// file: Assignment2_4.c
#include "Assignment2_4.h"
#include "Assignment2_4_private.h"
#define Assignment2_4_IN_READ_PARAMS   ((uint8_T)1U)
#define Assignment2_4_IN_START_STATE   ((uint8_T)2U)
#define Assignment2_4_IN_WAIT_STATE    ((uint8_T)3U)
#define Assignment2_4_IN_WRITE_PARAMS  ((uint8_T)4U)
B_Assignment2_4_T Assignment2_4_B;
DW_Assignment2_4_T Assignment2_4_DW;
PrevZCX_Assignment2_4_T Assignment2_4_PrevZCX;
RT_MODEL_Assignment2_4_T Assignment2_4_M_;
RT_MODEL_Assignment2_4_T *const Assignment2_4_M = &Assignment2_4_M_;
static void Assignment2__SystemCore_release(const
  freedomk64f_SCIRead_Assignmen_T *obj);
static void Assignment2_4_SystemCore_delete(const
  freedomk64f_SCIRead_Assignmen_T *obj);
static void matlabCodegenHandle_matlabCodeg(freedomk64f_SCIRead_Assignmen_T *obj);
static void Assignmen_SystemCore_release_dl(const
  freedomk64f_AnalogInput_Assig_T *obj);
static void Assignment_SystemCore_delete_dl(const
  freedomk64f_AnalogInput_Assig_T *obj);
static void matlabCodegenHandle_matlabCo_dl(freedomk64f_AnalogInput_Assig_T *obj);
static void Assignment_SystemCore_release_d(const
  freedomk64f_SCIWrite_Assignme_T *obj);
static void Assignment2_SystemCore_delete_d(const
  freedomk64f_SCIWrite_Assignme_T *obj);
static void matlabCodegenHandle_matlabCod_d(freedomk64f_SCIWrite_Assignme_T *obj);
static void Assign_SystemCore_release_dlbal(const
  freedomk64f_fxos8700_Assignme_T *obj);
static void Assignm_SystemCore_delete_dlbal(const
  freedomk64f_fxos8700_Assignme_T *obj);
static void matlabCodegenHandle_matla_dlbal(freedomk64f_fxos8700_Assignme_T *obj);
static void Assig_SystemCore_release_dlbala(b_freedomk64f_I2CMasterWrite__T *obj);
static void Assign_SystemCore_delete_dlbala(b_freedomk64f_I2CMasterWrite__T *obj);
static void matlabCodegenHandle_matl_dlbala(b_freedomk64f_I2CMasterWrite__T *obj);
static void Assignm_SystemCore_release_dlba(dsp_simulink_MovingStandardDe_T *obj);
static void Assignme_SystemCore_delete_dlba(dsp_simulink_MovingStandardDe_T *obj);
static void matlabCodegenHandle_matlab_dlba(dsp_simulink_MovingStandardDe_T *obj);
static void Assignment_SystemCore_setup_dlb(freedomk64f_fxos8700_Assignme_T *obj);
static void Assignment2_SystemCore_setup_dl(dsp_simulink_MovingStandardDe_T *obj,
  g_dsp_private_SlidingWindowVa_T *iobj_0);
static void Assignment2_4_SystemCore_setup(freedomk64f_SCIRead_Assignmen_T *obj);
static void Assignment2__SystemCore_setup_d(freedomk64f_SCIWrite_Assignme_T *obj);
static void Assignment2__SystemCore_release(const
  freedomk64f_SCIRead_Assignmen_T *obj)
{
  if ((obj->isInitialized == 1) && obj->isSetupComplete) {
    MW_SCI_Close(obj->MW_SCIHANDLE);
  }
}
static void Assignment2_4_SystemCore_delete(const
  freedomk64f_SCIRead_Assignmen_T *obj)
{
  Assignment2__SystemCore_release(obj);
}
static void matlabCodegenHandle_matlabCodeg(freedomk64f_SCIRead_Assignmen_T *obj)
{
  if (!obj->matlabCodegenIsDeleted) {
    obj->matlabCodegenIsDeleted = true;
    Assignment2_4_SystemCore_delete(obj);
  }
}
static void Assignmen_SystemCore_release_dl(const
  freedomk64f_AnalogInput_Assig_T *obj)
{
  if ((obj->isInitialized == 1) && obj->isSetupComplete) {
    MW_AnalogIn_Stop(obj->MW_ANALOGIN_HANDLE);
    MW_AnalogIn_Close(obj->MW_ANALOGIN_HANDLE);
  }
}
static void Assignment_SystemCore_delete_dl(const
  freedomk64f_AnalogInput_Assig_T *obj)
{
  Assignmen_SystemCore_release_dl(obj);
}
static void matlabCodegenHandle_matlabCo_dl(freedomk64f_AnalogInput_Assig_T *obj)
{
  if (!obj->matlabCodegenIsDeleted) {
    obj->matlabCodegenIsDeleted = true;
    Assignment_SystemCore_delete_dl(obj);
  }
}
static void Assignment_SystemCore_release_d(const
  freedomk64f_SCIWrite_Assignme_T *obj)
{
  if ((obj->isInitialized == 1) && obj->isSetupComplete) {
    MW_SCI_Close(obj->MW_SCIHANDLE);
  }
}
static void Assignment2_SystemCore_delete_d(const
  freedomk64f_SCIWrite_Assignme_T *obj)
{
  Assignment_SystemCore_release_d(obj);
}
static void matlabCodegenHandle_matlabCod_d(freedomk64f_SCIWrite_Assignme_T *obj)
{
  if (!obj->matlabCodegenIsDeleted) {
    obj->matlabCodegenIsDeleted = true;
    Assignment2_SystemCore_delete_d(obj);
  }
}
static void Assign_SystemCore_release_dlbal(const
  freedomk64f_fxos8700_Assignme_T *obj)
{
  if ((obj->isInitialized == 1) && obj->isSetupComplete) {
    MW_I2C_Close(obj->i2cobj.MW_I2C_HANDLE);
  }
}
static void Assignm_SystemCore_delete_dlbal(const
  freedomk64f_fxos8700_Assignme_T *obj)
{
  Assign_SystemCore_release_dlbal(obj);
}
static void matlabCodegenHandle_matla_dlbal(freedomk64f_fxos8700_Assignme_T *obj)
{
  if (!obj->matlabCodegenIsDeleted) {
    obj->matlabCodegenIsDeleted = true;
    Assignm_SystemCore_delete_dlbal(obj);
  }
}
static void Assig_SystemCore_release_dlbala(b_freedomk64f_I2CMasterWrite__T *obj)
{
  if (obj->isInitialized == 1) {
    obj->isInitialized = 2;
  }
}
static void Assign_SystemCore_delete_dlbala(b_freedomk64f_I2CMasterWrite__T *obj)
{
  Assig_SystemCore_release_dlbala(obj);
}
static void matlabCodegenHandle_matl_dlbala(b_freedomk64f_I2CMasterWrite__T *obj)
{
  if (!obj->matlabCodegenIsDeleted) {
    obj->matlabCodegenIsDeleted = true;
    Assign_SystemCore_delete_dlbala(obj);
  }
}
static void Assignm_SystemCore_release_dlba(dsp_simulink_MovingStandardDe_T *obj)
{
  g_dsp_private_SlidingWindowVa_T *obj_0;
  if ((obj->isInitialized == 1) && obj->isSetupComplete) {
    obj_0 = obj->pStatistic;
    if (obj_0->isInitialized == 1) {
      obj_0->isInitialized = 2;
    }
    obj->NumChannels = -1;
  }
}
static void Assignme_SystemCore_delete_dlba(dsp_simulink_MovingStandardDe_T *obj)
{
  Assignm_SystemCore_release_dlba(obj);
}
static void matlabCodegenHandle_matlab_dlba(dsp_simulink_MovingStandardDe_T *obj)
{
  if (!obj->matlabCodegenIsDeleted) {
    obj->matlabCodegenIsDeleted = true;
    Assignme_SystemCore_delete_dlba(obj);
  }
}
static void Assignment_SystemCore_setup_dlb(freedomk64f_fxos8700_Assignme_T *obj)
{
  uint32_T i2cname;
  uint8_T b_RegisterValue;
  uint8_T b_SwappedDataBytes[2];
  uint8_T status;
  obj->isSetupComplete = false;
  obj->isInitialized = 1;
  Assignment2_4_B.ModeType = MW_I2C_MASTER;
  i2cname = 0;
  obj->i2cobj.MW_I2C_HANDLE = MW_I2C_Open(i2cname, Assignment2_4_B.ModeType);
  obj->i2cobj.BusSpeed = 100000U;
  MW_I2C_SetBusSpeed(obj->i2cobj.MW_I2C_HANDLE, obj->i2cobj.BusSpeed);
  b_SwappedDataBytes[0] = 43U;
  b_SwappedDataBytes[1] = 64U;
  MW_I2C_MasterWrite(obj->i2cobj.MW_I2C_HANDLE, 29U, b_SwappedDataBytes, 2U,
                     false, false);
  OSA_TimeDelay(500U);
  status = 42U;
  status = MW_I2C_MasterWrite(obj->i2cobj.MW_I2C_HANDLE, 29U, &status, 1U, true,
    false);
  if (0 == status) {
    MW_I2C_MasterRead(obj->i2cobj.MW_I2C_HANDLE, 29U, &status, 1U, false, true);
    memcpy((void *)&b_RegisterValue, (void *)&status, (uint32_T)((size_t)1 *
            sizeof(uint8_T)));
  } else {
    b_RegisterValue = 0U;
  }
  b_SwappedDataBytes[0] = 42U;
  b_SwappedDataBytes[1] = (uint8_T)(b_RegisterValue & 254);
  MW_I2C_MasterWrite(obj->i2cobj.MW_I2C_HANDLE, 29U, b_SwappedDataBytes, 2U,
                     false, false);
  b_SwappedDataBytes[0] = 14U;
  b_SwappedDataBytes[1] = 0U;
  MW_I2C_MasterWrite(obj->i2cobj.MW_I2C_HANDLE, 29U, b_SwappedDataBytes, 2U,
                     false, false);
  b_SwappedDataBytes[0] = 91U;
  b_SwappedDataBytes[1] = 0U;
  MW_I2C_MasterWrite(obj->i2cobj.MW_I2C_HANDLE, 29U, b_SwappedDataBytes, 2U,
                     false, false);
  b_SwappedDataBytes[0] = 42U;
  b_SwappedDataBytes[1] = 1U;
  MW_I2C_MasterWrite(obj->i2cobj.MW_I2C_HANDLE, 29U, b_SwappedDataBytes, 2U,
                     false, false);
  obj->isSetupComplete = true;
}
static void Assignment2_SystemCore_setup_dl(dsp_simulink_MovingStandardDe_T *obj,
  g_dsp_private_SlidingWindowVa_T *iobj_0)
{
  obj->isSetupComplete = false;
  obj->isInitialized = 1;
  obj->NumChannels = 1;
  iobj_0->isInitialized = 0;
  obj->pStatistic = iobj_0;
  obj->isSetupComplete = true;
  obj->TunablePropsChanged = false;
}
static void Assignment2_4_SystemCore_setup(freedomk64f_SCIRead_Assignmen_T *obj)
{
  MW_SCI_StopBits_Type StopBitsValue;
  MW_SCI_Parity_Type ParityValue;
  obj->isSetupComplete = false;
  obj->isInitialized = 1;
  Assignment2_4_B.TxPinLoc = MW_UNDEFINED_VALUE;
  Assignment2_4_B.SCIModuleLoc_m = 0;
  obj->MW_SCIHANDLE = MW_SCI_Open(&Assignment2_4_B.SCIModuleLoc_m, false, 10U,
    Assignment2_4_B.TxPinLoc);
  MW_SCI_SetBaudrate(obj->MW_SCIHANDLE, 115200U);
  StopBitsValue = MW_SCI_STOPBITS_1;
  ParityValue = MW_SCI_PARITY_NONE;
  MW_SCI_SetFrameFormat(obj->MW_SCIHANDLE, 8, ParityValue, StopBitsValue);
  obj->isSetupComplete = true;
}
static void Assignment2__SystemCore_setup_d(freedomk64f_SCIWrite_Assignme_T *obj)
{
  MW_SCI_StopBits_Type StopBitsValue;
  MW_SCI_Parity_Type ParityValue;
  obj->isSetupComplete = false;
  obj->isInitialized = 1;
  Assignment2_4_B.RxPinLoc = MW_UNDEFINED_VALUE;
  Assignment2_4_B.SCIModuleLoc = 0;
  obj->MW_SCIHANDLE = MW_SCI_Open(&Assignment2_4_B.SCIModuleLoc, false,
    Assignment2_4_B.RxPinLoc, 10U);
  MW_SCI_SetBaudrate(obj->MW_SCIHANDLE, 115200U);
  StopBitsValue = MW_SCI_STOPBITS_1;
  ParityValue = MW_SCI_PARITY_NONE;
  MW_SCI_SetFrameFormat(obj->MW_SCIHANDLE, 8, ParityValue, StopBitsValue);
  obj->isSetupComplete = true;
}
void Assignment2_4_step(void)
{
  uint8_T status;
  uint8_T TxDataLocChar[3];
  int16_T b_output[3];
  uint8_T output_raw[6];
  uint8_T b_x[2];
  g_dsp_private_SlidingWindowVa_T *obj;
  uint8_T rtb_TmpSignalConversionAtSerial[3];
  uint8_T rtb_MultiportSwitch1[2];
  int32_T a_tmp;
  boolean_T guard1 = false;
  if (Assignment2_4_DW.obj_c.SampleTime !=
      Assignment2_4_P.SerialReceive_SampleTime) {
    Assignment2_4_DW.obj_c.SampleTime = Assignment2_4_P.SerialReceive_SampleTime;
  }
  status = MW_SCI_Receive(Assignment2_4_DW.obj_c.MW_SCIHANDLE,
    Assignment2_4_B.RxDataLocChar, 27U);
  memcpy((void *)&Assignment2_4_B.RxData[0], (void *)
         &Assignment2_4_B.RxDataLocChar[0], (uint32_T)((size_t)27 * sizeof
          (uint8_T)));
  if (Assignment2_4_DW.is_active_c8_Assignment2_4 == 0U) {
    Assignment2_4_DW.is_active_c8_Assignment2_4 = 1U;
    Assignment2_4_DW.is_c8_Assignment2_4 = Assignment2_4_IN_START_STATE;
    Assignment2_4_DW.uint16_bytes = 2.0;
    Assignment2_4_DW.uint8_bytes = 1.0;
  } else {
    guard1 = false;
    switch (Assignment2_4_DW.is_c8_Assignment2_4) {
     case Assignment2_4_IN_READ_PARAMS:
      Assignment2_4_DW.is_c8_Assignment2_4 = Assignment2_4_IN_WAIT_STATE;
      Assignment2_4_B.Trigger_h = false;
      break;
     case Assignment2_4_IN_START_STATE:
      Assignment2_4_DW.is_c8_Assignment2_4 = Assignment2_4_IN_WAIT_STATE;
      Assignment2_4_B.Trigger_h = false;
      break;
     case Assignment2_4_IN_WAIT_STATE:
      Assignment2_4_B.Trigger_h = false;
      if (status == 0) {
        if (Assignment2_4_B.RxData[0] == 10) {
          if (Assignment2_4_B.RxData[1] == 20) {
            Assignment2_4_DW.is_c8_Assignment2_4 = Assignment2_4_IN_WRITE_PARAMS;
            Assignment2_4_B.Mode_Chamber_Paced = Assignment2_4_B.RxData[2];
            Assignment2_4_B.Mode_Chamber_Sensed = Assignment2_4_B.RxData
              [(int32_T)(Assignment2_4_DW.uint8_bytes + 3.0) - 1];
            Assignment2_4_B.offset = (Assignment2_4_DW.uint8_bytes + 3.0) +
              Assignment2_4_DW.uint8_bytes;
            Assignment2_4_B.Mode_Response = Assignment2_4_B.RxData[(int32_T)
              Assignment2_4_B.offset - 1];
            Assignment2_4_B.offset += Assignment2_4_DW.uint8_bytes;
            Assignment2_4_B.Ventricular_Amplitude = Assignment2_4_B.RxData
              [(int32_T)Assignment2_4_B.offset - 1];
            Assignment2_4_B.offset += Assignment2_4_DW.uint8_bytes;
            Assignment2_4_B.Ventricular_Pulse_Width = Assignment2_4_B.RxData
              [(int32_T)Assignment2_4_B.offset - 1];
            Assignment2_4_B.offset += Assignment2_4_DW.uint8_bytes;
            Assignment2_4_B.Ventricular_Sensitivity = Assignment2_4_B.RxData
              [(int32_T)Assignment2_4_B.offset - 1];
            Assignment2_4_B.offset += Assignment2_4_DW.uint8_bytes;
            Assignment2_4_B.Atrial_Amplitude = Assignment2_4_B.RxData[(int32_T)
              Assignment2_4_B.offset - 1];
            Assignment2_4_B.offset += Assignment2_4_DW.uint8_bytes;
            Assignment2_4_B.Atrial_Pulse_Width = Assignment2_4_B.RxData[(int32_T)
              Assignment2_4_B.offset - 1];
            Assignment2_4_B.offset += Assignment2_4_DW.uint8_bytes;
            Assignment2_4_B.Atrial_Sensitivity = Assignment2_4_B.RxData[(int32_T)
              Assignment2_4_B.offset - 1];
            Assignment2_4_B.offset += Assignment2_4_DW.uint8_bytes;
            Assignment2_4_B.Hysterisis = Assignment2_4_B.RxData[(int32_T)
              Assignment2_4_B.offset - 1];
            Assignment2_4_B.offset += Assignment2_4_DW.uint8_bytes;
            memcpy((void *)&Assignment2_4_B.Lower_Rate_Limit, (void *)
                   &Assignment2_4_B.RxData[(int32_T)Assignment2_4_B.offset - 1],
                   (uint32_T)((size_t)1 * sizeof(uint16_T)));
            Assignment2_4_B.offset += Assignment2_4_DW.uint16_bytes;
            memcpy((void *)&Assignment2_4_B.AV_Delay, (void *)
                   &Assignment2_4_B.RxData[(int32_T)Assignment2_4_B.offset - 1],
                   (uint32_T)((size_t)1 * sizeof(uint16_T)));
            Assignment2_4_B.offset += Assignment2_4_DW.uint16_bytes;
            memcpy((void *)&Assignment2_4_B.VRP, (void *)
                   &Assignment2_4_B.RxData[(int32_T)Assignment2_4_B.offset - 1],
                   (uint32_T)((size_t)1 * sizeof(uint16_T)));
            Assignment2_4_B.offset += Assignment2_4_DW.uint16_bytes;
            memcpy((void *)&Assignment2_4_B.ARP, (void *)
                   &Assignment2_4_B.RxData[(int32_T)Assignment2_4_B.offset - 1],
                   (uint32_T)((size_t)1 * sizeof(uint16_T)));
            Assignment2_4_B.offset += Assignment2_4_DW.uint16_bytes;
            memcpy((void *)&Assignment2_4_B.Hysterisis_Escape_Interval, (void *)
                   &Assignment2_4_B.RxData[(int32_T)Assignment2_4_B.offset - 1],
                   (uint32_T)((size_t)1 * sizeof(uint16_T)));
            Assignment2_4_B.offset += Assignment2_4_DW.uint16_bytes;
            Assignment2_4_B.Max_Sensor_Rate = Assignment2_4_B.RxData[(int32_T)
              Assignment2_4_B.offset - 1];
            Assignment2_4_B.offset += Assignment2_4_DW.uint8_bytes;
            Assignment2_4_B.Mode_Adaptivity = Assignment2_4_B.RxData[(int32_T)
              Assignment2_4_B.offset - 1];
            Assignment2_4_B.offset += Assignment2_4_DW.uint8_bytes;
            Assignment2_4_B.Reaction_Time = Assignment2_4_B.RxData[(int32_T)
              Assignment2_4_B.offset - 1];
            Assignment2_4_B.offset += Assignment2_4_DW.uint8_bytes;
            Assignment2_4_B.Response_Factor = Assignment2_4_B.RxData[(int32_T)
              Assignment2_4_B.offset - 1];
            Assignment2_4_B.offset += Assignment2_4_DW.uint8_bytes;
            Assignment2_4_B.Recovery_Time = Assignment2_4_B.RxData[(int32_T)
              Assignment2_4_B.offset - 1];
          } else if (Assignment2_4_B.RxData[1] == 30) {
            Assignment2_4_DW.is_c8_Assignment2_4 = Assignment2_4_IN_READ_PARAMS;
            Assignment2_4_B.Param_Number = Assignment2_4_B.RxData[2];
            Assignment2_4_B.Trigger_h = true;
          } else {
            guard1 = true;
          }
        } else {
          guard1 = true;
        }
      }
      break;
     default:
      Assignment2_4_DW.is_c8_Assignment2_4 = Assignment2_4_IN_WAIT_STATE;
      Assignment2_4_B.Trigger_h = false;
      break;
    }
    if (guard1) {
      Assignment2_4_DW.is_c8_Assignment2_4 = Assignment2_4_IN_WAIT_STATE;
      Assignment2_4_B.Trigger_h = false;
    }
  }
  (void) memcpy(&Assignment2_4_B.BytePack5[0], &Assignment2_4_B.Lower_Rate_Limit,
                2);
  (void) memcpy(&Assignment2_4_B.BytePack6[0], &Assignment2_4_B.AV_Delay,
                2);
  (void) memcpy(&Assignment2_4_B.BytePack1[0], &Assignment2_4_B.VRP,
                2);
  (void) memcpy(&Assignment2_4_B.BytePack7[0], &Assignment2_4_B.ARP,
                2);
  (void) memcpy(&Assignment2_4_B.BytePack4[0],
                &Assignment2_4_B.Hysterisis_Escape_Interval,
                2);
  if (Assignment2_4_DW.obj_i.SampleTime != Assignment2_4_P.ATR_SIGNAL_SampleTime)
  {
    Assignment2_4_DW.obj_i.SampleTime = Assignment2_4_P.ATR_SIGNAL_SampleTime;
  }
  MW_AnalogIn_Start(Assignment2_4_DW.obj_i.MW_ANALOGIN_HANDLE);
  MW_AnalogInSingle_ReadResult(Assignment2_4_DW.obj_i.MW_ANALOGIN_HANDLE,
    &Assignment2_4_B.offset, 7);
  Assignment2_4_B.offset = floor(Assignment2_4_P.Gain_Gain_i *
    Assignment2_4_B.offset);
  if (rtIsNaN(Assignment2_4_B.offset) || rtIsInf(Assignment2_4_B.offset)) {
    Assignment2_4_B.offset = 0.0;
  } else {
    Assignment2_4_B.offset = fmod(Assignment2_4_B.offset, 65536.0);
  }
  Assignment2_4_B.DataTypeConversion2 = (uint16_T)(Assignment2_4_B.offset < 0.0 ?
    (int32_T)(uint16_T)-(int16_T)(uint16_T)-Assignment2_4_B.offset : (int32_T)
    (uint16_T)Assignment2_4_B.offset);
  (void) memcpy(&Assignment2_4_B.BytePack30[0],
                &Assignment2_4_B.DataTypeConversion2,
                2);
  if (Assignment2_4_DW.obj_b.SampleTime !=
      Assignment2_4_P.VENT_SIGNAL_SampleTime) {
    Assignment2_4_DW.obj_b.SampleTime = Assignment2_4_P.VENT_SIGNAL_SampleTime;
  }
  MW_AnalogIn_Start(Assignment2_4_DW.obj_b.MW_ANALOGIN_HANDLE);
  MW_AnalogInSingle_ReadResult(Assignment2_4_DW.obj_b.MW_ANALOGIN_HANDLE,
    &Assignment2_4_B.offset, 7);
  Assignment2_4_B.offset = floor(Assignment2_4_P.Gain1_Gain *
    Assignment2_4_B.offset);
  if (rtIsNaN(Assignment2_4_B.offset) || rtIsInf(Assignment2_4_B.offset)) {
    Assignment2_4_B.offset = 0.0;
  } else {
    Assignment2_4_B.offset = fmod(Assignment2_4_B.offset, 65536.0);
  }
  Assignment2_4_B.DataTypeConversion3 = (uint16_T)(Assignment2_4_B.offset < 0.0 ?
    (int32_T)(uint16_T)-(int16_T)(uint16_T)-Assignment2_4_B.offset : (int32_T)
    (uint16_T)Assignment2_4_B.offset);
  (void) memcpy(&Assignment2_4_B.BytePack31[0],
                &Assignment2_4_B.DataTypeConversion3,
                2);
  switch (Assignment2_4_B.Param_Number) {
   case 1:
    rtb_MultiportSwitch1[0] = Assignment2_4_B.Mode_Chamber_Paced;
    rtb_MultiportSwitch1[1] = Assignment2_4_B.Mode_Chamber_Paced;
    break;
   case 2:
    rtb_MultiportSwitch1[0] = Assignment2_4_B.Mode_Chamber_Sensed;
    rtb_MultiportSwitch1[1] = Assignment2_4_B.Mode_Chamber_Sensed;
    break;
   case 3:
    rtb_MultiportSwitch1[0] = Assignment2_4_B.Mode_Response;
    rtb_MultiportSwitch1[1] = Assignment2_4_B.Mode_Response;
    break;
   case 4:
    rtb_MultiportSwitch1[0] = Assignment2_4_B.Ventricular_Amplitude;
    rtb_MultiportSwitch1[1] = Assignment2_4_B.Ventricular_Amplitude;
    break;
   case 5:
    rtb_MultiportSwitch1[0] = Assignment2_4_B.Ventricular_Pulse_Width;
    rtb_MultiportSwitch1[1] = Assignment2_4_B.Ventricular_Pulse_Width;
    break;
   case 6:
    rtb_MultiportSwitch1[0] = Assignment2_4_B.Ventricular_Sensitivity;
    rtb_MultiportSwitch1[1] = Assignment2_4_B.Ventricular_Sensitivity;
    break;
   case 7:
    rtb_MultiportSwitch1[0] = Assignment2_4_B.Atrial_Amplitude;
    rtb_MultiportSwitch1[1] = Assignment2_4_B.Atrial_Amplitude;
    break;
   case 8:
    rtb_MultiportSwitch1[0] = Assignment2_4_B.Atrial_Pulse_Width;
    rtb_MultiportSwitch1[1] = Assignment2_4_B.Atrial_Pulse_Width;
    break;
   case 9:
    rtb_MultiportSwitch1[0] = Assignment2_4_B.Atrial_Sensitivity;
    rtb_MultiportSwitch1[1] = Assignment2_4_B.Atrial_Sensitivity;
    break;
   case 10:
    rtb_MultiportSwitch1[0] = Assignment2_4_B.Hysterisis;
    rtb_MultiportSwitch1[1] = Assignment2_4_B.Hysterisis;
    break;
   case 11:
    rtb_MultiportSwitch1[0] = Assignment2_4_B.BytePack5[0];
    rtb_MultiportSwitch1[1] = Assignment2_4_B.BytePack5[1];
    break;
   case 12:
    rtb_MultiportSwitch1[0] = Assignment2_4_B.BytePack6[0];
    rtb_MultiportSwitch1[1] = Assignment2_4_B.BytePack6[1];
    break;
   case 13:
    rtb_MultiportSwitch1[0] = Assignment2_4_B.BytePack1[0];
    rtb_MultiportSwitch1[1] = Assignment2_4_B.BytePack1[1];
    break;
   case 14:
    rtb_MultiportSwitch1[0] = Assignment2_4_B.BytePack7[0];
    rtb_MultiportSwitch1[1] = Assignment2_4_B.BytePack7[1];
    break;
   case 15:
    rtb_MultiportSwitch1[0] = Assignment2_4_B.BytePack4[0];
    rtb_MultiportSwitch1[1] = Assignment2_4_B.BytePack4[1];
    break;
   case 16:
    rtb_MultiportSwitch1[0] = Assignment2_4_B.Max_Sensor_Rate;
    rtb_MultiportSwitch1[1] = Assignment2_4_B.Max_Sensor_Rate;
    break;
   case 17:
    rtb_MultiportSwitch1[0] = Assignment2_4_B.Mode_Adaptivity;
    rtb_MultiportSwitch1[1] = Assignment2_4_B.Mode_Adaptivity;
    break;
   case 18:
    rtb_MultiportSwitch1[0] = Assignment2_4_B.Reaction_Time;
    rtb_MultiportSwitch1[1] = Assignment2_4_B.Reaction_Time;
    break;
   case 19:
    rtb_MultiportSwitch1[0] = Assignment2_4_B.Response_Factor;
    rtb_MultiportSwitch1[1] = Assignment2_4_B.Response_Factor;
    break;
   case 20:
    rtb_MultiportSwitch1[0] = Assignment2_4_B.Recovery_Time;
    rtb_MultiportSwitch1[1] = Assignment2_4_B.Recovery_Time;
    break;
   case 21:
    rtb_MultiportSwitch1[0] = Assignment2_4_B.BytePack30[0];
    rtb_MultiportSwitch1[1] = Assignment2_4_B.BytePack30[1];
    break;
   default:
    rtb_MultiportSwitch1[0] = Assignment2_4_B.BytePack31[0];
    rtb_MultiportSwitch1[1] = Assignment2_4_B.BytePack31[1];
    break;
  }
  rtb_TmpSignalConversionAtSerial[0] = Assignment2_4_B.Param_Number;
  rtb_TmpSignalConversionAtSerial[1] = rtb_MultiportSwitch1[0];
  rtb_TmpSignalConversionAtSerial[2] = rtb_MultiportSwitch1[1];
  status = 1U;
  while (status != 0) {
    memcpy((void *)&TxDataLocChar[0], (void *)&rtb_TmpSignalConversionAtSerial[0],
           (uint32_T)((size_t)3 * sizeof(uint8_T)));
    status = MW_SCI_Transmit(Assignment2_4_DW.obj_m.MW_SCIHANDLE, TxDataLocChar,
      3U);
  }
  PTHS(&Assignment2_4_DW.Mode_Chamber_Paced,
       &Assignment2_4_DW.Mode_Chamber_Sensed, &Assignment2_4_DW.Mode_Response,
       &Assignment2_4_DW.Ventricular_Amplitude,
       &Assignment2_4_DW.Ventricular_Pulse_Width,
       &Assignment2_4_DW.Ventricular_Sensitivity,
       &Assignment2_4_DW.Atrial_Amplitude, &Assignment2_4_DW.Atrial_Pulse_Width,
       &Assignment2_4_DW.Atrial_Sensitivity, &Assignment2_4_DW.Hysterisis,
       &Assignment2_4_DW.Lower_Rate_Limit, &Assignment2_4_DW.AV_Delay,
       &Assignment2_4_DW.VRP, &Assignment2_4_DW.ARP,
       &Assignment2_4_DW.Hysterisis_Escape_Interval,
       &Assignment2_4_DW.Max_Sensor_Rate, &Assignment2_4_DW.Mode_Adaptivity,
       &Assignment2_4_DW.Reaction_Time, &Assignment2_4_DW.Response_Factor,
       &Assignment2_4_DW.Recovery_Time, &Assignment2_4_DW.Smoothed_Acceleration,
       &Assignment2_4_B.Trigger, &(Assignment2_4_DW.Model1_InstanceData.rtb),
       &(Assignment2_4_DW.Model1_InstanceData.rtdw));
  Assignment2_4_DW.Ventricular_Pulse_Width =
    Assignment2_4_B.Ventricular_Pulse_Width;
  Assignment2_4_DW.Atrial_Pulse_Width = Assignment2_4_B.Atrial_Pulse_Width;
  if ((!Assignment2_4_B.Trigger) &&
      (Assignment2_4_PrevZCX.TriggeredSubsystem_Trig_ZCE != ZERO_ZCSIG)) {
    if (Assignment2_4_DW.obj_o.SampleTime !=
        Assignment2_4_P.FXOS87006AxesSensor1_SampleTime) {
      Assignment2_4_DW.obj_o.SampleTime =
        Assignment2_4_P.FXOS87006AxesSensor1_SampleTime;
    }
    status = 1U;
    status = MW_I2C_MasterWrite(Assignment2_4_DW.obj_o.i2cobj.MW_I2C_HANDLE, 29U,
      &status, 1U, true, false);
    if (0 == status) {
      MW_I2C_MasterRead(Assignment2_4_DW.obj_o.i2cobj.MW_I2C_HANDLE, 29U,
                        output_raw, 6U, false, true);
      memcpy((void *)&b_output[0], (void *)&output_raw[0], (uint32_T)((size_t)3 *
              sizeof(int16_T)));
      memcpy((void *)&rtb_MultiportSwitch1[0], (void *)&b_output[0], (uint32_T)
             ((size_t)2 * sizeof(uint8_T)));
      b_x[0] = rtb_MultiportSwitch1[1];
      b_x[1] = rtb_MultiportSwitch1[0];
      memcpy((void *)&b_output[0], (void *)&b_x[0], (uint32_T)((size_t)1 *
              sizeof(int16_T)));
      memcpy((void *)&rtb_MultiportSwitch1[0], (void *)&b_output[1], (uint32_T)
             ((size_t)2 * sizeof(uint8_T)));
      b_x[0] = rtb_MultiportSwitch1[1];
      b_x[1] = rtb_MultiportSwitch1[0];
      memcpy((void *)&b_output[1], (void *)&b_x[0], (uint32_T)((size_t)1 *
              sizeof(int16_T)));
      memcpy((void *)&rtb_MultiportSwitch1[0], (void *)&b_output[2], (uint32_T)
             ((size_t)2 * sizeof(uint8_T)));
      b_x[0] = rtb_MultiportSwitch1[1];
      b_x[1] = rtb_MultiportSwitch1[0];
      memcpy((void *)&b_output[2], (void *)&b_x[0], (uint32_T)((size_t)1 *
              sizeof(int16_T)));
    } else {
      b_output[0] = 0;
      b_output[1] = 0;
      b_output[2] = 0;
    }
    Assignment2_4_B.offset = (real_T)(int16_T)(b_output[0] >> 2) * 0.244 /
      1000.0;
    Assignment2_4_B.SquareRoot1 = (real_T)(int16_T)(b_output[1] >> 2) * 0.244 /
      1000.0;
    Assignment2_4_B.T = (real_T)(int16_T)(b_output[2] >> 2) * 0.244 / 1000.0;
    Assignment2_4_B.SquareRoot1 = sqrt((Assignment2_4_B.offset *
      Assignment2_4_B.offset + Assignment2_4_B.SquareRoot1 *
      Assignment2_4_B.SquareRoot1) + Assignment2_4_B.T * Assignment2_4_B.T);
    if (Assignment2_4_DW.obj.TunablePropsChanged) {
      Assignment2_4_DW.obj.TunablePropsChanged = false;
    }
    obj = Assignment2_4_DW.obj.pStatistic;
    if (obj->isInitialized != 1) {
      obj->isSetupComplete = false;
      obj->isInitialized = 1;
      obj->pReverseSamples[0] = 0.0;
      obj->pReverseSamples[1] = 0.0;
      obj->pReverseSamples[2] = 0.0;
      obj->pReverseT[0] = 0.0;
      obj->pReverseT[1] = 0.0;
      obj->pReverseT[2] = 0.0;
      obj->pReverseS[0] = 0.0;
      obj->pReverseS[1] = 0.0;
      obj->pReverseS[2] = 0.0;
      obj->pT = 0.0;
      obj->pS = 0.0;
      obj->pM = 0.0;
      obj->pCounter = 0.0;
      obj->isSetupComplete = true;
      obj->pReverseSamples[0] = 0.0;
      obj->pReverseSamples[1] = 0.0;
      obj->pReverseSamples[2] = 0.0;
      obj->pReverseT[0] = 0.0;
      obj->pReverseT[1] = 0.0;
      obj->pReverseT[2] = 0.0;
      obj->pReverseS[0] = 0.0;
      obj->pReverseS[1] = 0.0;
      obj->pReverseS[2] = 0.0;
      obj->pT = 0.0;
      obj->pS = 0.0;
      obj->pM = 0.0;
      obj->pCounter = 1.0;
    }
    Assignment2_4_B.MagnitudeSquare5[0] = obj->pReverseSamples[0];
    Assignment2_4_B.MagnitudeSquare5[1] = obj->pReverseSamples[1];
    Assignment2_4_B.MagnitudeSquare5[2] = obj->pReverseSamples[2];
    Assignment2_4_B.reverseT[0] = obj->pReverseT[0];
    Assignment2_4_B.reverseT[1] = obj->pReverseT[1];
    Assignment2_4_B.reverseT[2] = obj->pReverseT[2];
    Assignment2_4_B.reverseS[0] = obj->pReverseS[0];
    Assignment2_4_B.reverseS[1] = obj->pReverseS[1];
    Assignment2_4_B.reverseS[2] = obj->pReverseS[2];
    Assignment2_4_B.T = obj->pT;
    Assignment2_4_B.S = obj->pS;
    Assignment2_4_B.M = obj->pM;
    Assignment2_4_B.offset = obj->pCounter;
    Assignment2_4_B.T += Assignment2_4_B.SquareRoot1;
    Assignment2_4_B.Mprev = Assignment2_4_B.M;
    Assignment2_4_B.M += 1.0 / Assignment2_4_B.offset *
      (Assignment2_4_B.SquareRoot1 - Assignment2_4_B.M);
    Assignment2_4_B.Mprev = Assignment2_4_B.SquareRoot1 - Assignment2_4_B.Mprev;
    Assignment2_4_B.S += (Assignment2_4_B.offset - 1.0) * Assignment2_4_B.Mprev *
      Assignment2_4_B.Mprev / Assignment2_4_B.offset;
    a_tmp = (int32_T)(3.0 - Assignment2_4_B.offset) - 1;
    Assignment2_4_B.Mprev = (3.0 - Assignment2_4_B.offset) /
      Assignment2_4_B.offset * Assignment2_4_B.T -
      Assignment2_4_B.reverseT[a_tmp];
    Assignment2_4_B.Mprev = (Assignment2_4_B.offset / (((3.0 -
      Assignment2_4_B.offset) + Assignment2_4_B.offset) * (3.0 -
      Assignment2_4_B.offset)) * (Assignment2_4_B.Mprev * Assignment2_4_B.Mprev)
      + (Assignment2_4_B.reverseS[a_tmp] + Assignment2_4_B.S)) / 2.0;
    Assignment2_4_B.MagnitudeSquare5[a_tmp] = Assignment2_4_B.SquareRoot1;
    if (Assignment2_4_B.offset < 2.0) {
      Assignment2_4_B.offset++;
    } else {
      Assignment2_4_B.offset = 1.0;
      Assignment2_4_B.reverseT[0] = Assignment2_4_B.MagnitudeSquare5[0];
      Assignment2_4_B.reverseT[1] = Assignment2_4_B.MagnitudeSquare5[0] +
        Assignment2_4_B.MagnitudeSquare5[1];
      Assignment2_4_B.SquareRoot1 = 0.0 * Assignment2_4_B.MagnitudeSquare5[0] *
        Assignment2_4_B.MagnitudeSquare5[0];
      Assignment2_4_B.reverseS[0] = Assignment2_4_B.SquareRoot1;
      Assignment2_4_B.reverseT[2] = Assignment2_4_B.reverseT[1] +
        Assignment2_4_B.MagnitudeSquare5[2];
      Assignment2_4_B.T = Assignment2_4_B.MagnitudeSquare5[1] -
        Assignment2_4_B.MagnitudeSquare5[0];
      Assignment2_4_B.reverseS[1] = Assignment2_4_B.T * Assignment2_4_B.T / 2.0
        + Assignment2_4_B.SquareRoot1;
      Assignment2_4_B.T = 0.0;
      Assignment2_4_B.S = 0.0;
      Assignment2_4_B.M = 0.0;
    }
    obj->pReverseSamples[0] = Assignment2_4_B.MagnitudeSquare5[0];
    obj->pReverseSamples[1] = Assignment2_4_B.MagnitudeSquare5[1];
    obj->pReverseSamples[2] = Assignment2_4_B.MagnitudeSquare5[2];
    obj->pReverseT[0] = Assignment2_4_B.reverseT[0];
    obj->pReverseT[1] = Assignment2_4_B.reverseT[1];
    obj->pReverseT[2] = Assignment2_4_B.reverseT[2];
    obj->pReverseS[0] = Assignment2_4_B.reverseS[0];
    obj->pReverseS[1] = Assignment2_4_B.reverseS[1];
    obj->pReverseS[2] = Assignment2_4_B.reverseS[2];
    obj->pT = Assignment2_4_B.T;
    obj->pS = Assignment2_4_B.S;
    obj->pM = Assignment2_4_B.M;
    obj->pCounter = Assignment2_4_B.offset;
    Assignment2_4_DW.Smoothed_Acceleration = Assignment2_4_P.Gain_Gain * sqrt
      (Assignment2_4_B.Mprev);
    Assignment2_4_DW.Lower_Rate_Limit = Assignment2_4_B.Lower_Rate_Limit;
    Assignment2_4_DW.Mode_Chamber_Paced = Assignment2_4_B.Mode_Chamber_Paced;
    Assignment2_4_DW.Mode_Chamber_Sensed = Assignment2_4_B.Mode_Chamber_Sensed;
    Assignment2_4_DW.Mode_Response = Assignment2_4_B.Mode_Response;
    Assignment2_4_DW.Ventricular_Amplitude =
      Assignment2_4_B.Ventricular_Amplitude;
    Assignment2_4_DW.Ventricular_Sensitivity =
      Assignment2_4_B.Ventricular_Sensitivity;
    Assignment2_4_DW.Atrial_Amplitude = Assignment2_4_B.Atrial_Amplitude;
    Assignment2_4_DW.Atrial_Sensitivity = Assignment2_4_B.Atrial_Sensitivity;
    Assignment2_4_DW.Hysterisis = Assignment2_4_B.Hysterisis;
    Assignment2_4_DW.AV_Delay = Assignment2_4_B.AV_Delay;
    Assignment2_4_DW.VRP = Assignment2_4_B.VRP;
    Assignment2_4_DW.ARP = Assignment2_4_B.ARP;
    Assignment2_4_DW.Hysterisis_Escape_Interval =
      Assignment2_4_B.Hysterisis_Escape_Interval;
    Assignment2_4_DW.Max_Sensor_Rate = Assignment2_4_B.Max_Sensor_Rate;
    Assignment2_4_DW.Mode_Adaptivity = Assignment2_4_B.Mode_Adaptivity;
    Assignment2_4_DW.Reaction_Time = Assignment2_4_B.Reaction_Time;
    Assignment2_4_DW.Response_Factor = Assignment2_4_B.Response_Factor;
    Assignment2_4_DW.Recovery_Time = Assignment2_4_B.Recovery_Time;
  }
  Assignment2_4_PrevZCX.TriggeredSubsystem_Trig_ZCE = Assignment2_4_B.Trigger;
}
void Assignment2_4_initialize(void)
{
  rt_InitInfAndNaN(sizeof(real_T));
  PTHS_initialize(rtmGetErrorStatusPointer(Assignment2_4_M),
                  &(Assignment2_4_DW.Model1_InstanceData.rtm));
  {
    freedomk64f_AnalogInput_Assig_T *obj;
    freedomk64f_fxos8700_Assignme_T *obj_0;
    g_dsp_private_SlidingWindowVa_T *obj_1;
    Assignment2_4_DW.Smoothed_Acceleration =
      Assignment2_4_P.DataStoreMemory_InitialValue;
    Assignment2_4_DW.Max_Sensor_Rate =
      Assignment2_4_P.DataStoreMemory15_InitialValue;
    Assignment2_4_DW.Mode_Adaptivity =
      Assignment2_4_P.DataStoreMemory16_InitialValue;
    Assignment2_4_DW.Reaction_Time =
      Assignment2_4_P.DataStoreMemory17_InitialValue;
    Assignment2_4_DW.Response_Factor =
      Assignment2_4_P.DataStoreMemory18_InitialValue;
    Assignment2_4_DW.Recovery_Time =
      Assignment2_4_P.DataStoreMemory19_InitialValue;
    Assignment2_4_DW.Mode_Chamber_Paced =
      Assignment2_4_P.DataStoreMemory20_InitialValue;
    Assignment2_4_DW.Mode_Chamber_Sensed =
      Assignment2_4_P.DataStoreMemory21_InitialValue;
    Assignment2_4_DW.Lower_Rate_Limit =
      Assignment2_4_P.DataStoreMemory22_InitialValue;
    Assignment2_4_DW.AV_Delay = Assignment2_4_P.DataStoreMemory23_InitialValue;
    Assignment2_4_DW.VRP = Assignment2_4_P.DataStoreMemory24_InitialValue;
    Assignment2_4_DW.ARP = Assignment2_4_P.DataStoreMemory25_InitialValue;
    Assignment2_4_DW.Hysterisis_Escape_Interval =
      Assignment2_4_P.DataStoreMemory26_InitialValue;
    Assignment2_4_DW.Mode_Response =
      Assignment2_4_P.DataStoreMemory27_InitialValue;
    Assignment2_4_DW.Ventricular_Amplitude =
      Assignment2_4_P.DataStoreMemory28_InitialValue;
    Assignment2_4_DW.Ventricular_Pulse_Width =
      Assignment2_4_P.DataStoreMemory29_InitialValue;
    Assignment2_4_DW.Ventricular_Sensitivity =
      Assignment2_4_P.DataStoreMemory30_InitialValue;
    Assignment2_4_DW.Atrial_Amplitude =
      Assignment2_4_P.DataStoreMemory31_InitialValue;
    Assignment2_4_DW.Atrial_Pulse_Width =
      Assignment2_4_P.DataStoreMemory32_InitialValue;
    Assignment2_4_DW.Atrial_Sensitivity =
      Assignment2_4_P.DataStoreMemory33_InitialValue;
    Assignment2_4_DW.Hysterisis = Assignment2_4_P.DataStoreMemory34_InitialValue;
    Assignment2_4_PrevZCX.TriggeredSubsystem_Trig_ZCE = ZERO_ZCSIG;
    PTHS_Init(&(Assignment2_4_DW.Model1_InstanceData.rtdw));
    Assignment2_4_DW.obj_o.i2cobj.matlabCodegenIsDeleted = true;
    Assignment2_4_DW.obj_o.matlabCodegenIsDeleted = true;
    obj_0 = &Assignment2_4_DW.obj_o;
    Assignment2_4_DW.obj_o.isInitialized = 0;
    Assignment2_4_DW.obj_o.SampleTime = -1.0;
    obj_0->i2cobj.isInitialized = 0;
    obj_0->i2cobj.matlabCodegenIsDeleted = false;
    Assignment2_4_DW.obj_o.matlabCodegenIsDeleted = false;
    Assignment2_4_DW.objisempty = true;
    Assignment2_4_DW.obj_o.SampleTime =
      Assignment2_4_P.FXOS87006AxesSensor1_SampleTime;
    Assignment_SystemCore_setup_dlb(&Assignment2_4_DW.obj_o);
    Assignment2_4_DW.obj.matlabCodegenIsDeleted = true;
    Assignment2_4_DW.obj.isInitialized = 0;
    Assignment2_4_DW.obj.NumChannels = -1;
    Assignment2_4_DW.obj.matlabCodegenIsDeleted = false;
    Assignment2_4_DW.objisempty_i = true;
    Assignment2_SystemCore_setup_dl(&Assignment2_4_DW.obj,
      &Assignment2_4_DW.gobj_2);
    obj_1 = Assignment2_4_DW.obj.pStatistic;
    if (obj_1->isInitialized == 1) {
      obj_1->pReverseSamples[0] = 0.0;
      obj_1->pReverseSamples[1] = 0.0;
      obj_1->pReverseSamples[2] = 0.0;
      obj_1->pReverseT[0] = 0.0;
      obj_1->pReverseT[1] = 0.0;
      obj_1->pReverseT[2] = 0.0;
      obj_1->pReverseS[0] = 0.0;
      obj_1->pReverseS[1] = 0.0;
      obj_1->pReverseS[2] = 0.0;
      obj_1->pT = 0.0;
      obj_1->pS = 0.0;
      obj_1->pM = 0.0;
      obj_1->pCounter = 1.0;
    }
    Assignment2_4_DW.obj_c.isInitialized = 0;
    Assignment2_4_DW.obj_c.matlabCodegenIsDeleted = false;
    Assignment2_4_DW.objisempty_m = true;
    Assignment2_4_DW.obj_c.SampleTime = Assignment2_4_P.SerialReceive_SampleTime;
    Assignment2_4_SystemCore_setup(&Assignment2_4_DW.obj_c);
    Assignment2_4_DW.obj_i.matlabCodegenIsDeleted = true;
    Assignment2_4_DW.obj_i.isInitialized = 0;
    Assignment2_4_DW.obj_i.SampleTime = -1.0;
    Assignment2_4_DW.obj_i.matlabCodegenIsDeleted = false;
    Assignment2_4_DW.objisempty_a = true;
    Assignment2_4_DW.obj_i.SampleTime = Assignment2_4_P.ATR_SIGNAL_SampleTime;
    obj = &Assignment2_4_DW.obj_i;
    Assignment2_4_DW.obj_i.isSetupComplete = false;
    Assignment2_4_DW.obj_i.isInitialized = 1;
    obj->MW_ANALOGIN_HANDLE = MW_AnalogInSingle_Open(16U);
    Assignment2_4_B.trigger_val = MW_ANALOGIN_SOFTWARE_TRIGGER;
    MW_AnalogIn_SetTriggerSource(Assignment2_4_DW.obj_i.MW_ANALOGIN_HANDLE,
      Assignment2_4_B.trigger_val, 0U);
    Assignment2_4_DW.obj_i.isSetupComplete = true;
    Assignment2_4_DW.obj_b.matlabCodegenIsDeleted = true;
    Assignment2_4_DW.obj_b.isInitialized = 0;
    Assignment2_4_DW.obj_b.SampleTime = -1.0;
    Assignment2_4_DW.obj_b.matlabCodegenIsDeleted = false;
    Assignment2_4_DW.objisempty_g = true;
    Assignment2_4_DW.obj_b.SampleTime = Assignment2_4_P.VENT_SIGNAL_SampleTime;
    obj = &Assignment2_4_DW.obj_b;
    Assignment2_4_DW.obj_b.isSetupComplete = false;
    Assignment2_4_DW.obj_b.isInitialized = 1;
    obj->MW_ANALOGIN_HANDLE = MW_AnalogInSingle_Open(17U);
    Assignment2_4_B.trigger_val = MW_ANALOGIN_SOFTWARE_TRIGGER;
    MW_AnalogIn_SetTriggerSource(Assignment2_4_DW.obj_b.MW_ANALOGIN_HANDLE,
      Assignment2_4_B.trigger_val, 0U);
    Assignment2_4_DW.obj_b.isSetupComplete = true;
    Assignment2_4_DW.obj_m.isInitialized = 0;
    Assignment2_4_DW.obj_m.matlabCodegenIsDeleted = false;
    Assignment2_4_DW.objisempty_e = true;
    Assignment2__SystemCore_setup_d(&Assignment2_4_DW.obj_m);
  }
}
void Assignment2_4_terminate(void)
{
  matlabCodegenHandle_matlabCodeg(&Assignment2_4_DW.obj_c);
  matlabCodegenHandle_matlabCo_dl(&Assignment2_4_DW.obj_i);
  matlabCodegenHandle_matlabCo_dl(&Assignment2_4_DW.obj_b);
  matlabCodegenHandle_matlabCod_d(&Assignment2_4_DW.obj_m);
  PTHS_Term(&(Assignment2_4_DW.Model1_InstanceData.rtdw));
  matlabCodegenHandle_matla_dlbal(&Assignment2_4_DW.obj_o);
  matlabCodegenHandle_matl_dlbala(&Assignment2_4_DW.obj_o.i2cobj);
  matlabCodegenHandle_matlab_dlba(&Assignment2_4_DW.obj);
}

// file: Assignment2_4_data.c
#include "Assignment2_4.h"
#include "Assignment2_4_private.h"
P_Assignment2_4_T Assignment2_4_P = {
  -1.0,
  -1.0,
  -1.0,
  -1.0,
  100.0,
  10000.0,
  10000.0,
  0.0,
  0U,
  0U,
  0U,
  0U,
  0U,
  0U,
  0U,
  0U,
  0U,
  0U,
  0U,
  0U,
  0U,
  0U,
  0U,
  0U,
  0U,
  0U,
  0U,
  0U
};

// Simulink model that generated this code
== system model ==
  SerialTransmit#1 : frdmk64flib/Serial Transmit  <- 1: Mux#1
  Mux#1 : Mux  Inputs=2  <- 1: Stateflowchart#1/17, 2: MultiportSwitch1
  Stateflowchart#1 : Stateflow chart  <- 1: SerialReceive, 2: SerialReceive/2
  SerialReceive : frdmk64flib/Serial Receive
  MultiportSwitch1 : MultiPortSwitch  Inputs=22  <- 1: Stateflowchart#1/17, 2: Stateflowchart#1/2, 3: Stateflowchart#1/3, 4: Stateflowchart#1/4, 5: Stateflowchart#1/5, 6: Stateflowchart#1/6, 7: Stateflowchart#1/7, 8: Stateflowchart#1/8, 9: Stateflowchart#1/9, 10: Stateflowchart#1/10, 11: Stateflowchart#1/11, 12: BytePack5, 13: BytePack6, 14: BytePack1, 15: BytePack7, 16: BytePack4, 17: Stateflowchart#1/18, 18: Stateflowchart#1/19, 19: Stateflowchart#1/20, 20: Stateflowchart#1/21, 21: Stateflowchart#1/22, 22: BytePack30, 23: BytePack31
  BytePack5 : etargetslib/Byte Pack  <- 1: Stateflowchart#1/12
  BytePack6 : etargetslib/Byte Pack  <- 1: Stateflowchart#1/13
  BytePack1 : etargetslib/Byte Pack  <- 1: Stateflowchart#1/14
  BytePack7 : etargetslib/Byte Pack  <- 1: Stateflowchart#1/15
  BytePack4 : etargetslib/Byte Pack  <- 1: Stateflowchart#1/16
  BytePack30 : etargetslib/Byte Pack  <- 1: DataTypeConversion2
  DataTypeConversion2 : DataTypeConversion  <- 1: Gain
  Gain : Gain  Gain=10000  <- 1: ATR_SIGNAL
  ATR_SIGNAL : frdmk64flib/Analog Input
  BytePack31 : etargetslib/Byte Pack  <- 1: DataTypeConversion3
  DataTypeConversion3 : DataTypeConversion  <- 1: Gain1
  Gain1 : Gain  Gain=10000  <- 1: VENT_SIGNAL
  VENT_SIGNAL : frdmk64flib/Analog Input
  TriggeredSubsystem : Subsystem  <- 1: Stateflowchart#1/2, 2: Stateflowchart#1/3, 3: Stateflowchart#1/4, 4: Stateflowchart#1/5, 5: DataTypeConversion#1, 6: Stateflowchart#1/7, 7: Stateflowchart#1/8, 8: DataTypeConversion#2, 9: Stateflowchart#1/10, 10: Stateflowchart#1/11, 11: Stateflowchart#1/12, 12: Stateflowchart#1/13, 13: Stateflowchart#1/14, 14: Stateflowchart#1/15, 15: Stateflowchart#1/16, 16: Stateflowchart#1/18, 17: Stateflowchart#1/19, 18: Stateflowchart#1/20, 19: Stateflowchart#1/21, 20: Stateflowchart#1/22, Trigger: Model1
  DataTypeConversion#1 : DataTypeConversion  <- 1: Stateflowchart#1/6
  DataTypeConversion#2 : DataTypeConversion  <- 1: Stateflowchart#1/9
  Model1 : ModelReference  <- 1: DataStoreRead#1, 2: DataStoreRead#2, 3: DataStoreRead#3, 4: DataStoreRead#4, 5: DataStoreRead#5, 6: DataStoreRead#6, 7: DataStoreRead#7, 8: DataStoreRead#8, 9: DataStoreRead#9, 10: DataStoreRead#10, 11: DataStoreRead#11, 12: DataStoreRead#12, 13: DataStoreRead#13, 14: DataStoreRead#14, 15: DataStoreRead#15, 16: DataStoreRead#16, 17: DataStoreRead#17, 18: DataStoreRead#18, 19: DataStoreRead#19, 20: DataStoreRead#20, 21: DataStoreRead#21
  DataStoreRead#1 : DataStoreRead  DataStoreName=Mode_Chamber_Paced
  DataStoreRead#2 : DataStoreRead  DataStoreName=Mode_Chamber_Sensed
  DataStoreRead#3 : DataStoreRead  DataStoreName=Mode_Response
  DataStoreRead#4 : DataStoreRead  DataStoreName=Ventricular_Amplitude
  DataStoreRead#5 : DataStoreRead  DataStoreName=Ventricular_Pulse_Width
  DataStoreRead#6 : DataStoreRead  DataStoreName=Ventricular_Sensitivity
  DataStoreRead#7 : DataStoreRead  DataStoreName=Atrial_Amplitude
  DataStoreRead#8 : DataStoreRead  DataStoreName=Atrial_Pulse_Width
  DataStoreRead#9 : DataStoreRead  DataStoreName=Atrial_Sensitivity
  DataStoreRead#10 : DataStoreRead  DataStoreName=Hysterisis
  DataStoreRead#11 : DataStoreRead  DataStoreName=Lower_Rate_Limit
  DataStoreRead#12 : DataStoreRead  DataStoreName=AV_Delay
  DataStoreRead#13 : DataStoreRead  DataStoreName=VRP
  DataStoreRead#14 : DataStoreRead  DataStoreName=ARP
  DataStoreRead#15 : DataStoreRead  DataStoreName=Hysterisis_Escape_Interval
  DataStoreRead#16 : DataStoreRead  DataStoreName=Max_Sensor_Rate
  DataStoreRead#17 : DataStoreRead  DataStoreName=Mode_Adaptivity
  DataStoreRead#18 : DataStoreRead  DataStoreName=Reaction_Time
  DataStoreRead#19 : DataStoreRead  DataStoreName=Response_Factor
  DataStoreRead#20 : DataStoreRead  DataStoreName=Recovery_Time
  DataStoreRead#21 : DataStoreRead  DataStoreName=Smoothed_Acceleration
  DataStoreMemory : DataStoreMemory  DataStoreName=Smoothed_Acceleration
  DataStoreMemory15 : DataStoreMemory  DataStoreName=Max_Sensor_Rate
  DataStoreMemory16 : DataStoreMemory  DataStoreName=Mode_Adaptivity
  DataStoreMemory17 : DataStoreMemory  DataStoreName=Reaction_Time
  DataStoreMemory18 : DataStoreMemory  DataStoreName=Response_Factor
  DataStoreMemory19 : DataStoreMemory  DataStoreName=Recovery_Time
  DataStoreMemory20 : DataStoreMemory  DataStoreName=Mode_Chamber_Paced
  DataStoreMemory21 : DataStoreMemory  DataStoreName=Mode_Chamber_Sensed
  DataStoreMemory22 : DataStoreMemory  DataStoreName=Lower_Rate_Limit
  DataStoreMemory23 : DataStoreMemory  DataStoreName=AV_Delay
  DataStoreMemory24 : DataStoreMemory  DataStoreName=VRP
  DataStoreMemory25 : DataStoreMemory  DataStoreName=ARP
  DataStoreMemory26 : DataStoreMemory  DataStoreName=Hysterisis_Escape_Interval
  DataStoreMemory27 : DataStoreMemory  DataStoreName=Mode_Response
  DataStoreMemory28 : DataStoreMemory  DataStoreName=Ventricular_Amplitude
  DataStoreMemory29 : DataStoreMemory  DataStoreName=Ventricular_Pulse_Width
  DataStoreMemory30 : DataStoreMemory  DataStoreName=Ventricular_Sensitivity
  DataStoreMemory31 : DataStoreMemory  DataStoreName=Atrial_Amplitude
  DataStoreMemory32 : DataStoreMemory  DataStoreName=Atrial_Pulse_Width
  DataStoreMemory33 : DataStoreMemory  DataStoreName=Atrial_Sensitivity
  DataStoreMemory34 : DataStoreMemory  DataStoreName=Hysterisis
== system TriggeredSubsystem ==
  Mode_Chamber_Paced : Inport
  Mode_Chamber_Sensed : Inport
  Mode_Response : Inport
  Inport#1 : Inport
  Ventricular_Pulse_Width : Inport
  Inport#2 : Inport
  Atrial_Amplitude : Inport
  Atrial_Pulse_Width : Inport
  Atrial_Sensitivity : Inport
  Hysterisis : Inport
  Lower_Rate_Limit : Inport
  AV_Delay : Inport
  VRP : Inport
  ARP : Inport
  Hysterisis_Escape_Interval : Inport
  Max_Sensor_Rate : Inport
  Mode_Adaptivity : Inport
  Reaction_Time : Inport
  Response_Factor : Inport
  Recovery_Time : Inport
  Trigger : TriggerPort  TriggerType=falling
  DataStoreWrite#1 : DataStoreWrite  DataStoreName=Ventricular_Pulse_Width  <- 1: Ventricular_Pulse_Width
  DataStoreWrite#2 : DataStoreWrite  DataStoreName=Atrial_Pulse_Width  <- 1: Atrial_Pulse_Width
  DataStoreWrite#3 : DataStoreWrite  DataStoreName=Smoothed_Acceleration  <- 1: Gain#1
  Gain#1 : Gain  Gain=100  <- 1: MovingStandardDeviation#1
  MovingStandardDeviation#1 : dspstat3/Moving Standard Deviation  <- 1: SquareRoot1
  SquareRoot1 : Sqrt  <- 1: Sum#1
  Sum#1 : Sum  Inputs=+  <- 1: MagnitudeSquare5
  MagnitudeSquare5 : Math  Operator=magnitude^2  <- 1: FXOS87006AxesSensor1
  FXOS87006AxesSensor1 : frdmk64flib/FXOS8700 6-Axes Sensor
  DataStoreWrite#4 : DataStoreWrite  DataStoreName=Lower_Rate_Limit  <- 1: DataTypeConversion#3
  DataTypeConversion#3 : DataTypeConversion  <- 1: DataTypeConversion#4
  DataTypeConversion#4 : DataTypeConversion  <- 1: Lower_Rate_Limit
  DataStoreWrite#5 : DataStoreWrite  DataStoreName=Mode_Chamber_Paced  <- 1: Mode_Chamber_Paced
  DataStoreWrite#6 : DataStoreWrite  DataStoreName=Mode_Chamber_Sensed  <- 1: Mode_Chamber_Sensed
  DataStoreWrite#7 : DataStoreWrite  DataStoreName=Mode_Response  <- 1: Mode_Response
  DataStoreWrite#8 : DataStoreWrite  DataStoreName=Ventricular_Amplitude  <- 1: Inport#1
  DataStoreWrite#9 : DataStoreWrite  DataStoreName=Ventricular_Sensitivity  <- 1: Inport#2
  DataStoreWrite#10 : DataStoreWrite  DataStoreName=Atrial_Amplitude  <- 1: Atrial_Amplitude
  DataStoreWrite#11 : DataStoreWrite  DataStoreName=Atrial_Sensitivity  <- 1: Atrial_Sensitivity
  DataStoreWrite#12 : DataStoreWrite  DataStoreName=Hysterisis  <- 1: Hysterisis
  DataStoreWrite#13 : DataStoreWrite  DataStoreName=AV_Delay  <- 1: AV_Delay
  DataStoreWrite#14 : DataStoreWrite  DataStoreName=VRP  <- 1: VRP
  DataStoreWrite#15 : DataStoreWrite  DataStoreName=ARP  <- 1: ARP
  DataStoreWrite#16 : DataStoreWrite  DataStoreName=Hysterisis_Escape_Interval  <- 1: Hysterisis_Escape_Interval
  DataStoreWrite#17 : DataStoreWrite  DataStoreName=Max_Sensor_Rate  <- 1: Max_Sensor_Rate
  DataStoreWrite#18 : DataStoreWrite  DataStoreName=Mode_Adaptivity  <- 1: Mode_Adaptivity
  DataStoreWrite#19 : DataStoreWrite  DataStoreName=Reaction_Time  <- 1: Reaction_Time
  DataStoreWrite#20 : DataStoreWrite  DataStoreName=Response_Factor  <- 1: Response_Factor
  DataStoreWrite#21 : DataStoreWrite  DataStoreName=Recovery_Time  <- 1: Recovery_Time
== stateflow chart Stateflowchart#1 ==
  state WRITE_PARAMS
    entry:
    %See Serial Protocol section in Part 1 of documentation
    %OFFSET
    %A local variable offset is used to index rx instead of raw numbers
    offset=3;
    %MODES
    Mode_Chamber_Paced=rx(offset);
    offset=offset+uint8_bytes;
    Mode_Chamber_Sensed=rx(offset);
    offset=offset+uint8_bytes;
    Mode_Response=rx(offset);
    offset=offset+uint8_bytes;
    %VENTRICLULAR PACE PARAMS
    Ventricular_Amplitude=rx(offset);
    offset=offset+uint8_bytes;
    Ventricular_Pulse_Width=rx(offset);
    offset=offset+uint8_bytes;
    Ventricular_Sensitivity=rx(offset);
    offset=offset+uint8_bytes;
    %ATRIAL PACE PARAMS
    Atrial_Amplitude=rx(offset);
    offset=offset+uint8_bytes;
    Atrial_Pulse_Width=rx(offset);
    offset=offset+uint8_bytes;
    Atrial_Sensitivity=rx(offset);
    offset=offset+uint8_bytes;
    %HYSTERISIS
    Hysterisis=rx(offset);
    offset=offset+uint8_bytes;
    %uint16 PARAMETERS
    Lower_Rate_Limit=typecast(rx(offset:offset+1),'uint16');
    offset=offset+uint16_bytes;
    AV_Delay=typecast(rx(offset:offset+1),'uint16');
    offset=offset+uint16_bytes;
    VRP=typecast(rx(offset:offset+1),'uint16');
    offset=offset+uint16_bytes;
    ARP=typecast(rx(offset:offset+1),'uint16');
    offset=offset+uint16_bytes;
    Hysterisis_Escape_Interval=typecast(rx(offset:offset+1),'uint16');
    offset=offset+uint16_bytes;
    %RATE ADAPTIVITY
    Max_Sensor_Rate = rx(offset);
    offset=offset+uint8_bytes;
    Mode_Adaptivity = rx(offset);
    offset=offset+uint8_bytes;
    Reaction_Time=rx(offset);
    offset=offset+uint8_bytes;
    Response_Factor = rx(offset);
    offset=offset+uint8_bytes;
    Recovery_Time =  rx(offset);
    offset=offset+uint8_bytes;
  note: TEST_CODE: 10
      | SET_CODE: 20
      | ECHO_CODE: 30
  state START_STATE
    entry:
    uint16_bytes = 2;
    uint8_bytes = 1;
    single_bytes=4;
  state WAIT_STATE
    entry:
    Trigger = false;
  state READ_PARAMS
    entry:
    %See Serial Protocol section in Part 1 of documentation
    Param_Number=rx(3);
    Trigger = true;
  WRITE_PARAMS -> WAIT_STATE
  (junction 199) -> WRITE_PARAMS [order 1] : [rx(2)==20]
  (default) -> START_STATE
  (junction 132) -> WAIT_STATE [order 2]
  START_STATE -> WAIT_STATE
  WAIT_STATE -> (junction 132) : [status == 0]
  (junction 132) -> (junction 199) [order 1] : [rx(1)==10]
  (junction 199) -> READ_PARAMS [order 2] : [rx(2) == 30]
  READ_PARAMS -> WAIT_STATE
  data: Trigger output; Mode_Chamber_Paced output; Mode_Chamber_Sensed output; Mode_Response output; Ventricular_Amplitude output; Ventricular_Pulse_Width output; Ventricular_Sensitivity output; Atrial_Amplitude output; rx input uint8; offset local; Atrial_Pulse_Width output; Atrial_Sensitivity output; Hysterisis output; Lower_Rate_Limit output; AV_Delay output; VRP output; ARP output; Hysterisis_Escape_Interval output; status input uint8; uint16_bytes local; uint8_bytes local; single_bytes local; Param_Number output; Max_Sensor_Rate output; Mode_Adaptivity output; Reaction_Time output; Response_Factor output; Recovery_Time output
